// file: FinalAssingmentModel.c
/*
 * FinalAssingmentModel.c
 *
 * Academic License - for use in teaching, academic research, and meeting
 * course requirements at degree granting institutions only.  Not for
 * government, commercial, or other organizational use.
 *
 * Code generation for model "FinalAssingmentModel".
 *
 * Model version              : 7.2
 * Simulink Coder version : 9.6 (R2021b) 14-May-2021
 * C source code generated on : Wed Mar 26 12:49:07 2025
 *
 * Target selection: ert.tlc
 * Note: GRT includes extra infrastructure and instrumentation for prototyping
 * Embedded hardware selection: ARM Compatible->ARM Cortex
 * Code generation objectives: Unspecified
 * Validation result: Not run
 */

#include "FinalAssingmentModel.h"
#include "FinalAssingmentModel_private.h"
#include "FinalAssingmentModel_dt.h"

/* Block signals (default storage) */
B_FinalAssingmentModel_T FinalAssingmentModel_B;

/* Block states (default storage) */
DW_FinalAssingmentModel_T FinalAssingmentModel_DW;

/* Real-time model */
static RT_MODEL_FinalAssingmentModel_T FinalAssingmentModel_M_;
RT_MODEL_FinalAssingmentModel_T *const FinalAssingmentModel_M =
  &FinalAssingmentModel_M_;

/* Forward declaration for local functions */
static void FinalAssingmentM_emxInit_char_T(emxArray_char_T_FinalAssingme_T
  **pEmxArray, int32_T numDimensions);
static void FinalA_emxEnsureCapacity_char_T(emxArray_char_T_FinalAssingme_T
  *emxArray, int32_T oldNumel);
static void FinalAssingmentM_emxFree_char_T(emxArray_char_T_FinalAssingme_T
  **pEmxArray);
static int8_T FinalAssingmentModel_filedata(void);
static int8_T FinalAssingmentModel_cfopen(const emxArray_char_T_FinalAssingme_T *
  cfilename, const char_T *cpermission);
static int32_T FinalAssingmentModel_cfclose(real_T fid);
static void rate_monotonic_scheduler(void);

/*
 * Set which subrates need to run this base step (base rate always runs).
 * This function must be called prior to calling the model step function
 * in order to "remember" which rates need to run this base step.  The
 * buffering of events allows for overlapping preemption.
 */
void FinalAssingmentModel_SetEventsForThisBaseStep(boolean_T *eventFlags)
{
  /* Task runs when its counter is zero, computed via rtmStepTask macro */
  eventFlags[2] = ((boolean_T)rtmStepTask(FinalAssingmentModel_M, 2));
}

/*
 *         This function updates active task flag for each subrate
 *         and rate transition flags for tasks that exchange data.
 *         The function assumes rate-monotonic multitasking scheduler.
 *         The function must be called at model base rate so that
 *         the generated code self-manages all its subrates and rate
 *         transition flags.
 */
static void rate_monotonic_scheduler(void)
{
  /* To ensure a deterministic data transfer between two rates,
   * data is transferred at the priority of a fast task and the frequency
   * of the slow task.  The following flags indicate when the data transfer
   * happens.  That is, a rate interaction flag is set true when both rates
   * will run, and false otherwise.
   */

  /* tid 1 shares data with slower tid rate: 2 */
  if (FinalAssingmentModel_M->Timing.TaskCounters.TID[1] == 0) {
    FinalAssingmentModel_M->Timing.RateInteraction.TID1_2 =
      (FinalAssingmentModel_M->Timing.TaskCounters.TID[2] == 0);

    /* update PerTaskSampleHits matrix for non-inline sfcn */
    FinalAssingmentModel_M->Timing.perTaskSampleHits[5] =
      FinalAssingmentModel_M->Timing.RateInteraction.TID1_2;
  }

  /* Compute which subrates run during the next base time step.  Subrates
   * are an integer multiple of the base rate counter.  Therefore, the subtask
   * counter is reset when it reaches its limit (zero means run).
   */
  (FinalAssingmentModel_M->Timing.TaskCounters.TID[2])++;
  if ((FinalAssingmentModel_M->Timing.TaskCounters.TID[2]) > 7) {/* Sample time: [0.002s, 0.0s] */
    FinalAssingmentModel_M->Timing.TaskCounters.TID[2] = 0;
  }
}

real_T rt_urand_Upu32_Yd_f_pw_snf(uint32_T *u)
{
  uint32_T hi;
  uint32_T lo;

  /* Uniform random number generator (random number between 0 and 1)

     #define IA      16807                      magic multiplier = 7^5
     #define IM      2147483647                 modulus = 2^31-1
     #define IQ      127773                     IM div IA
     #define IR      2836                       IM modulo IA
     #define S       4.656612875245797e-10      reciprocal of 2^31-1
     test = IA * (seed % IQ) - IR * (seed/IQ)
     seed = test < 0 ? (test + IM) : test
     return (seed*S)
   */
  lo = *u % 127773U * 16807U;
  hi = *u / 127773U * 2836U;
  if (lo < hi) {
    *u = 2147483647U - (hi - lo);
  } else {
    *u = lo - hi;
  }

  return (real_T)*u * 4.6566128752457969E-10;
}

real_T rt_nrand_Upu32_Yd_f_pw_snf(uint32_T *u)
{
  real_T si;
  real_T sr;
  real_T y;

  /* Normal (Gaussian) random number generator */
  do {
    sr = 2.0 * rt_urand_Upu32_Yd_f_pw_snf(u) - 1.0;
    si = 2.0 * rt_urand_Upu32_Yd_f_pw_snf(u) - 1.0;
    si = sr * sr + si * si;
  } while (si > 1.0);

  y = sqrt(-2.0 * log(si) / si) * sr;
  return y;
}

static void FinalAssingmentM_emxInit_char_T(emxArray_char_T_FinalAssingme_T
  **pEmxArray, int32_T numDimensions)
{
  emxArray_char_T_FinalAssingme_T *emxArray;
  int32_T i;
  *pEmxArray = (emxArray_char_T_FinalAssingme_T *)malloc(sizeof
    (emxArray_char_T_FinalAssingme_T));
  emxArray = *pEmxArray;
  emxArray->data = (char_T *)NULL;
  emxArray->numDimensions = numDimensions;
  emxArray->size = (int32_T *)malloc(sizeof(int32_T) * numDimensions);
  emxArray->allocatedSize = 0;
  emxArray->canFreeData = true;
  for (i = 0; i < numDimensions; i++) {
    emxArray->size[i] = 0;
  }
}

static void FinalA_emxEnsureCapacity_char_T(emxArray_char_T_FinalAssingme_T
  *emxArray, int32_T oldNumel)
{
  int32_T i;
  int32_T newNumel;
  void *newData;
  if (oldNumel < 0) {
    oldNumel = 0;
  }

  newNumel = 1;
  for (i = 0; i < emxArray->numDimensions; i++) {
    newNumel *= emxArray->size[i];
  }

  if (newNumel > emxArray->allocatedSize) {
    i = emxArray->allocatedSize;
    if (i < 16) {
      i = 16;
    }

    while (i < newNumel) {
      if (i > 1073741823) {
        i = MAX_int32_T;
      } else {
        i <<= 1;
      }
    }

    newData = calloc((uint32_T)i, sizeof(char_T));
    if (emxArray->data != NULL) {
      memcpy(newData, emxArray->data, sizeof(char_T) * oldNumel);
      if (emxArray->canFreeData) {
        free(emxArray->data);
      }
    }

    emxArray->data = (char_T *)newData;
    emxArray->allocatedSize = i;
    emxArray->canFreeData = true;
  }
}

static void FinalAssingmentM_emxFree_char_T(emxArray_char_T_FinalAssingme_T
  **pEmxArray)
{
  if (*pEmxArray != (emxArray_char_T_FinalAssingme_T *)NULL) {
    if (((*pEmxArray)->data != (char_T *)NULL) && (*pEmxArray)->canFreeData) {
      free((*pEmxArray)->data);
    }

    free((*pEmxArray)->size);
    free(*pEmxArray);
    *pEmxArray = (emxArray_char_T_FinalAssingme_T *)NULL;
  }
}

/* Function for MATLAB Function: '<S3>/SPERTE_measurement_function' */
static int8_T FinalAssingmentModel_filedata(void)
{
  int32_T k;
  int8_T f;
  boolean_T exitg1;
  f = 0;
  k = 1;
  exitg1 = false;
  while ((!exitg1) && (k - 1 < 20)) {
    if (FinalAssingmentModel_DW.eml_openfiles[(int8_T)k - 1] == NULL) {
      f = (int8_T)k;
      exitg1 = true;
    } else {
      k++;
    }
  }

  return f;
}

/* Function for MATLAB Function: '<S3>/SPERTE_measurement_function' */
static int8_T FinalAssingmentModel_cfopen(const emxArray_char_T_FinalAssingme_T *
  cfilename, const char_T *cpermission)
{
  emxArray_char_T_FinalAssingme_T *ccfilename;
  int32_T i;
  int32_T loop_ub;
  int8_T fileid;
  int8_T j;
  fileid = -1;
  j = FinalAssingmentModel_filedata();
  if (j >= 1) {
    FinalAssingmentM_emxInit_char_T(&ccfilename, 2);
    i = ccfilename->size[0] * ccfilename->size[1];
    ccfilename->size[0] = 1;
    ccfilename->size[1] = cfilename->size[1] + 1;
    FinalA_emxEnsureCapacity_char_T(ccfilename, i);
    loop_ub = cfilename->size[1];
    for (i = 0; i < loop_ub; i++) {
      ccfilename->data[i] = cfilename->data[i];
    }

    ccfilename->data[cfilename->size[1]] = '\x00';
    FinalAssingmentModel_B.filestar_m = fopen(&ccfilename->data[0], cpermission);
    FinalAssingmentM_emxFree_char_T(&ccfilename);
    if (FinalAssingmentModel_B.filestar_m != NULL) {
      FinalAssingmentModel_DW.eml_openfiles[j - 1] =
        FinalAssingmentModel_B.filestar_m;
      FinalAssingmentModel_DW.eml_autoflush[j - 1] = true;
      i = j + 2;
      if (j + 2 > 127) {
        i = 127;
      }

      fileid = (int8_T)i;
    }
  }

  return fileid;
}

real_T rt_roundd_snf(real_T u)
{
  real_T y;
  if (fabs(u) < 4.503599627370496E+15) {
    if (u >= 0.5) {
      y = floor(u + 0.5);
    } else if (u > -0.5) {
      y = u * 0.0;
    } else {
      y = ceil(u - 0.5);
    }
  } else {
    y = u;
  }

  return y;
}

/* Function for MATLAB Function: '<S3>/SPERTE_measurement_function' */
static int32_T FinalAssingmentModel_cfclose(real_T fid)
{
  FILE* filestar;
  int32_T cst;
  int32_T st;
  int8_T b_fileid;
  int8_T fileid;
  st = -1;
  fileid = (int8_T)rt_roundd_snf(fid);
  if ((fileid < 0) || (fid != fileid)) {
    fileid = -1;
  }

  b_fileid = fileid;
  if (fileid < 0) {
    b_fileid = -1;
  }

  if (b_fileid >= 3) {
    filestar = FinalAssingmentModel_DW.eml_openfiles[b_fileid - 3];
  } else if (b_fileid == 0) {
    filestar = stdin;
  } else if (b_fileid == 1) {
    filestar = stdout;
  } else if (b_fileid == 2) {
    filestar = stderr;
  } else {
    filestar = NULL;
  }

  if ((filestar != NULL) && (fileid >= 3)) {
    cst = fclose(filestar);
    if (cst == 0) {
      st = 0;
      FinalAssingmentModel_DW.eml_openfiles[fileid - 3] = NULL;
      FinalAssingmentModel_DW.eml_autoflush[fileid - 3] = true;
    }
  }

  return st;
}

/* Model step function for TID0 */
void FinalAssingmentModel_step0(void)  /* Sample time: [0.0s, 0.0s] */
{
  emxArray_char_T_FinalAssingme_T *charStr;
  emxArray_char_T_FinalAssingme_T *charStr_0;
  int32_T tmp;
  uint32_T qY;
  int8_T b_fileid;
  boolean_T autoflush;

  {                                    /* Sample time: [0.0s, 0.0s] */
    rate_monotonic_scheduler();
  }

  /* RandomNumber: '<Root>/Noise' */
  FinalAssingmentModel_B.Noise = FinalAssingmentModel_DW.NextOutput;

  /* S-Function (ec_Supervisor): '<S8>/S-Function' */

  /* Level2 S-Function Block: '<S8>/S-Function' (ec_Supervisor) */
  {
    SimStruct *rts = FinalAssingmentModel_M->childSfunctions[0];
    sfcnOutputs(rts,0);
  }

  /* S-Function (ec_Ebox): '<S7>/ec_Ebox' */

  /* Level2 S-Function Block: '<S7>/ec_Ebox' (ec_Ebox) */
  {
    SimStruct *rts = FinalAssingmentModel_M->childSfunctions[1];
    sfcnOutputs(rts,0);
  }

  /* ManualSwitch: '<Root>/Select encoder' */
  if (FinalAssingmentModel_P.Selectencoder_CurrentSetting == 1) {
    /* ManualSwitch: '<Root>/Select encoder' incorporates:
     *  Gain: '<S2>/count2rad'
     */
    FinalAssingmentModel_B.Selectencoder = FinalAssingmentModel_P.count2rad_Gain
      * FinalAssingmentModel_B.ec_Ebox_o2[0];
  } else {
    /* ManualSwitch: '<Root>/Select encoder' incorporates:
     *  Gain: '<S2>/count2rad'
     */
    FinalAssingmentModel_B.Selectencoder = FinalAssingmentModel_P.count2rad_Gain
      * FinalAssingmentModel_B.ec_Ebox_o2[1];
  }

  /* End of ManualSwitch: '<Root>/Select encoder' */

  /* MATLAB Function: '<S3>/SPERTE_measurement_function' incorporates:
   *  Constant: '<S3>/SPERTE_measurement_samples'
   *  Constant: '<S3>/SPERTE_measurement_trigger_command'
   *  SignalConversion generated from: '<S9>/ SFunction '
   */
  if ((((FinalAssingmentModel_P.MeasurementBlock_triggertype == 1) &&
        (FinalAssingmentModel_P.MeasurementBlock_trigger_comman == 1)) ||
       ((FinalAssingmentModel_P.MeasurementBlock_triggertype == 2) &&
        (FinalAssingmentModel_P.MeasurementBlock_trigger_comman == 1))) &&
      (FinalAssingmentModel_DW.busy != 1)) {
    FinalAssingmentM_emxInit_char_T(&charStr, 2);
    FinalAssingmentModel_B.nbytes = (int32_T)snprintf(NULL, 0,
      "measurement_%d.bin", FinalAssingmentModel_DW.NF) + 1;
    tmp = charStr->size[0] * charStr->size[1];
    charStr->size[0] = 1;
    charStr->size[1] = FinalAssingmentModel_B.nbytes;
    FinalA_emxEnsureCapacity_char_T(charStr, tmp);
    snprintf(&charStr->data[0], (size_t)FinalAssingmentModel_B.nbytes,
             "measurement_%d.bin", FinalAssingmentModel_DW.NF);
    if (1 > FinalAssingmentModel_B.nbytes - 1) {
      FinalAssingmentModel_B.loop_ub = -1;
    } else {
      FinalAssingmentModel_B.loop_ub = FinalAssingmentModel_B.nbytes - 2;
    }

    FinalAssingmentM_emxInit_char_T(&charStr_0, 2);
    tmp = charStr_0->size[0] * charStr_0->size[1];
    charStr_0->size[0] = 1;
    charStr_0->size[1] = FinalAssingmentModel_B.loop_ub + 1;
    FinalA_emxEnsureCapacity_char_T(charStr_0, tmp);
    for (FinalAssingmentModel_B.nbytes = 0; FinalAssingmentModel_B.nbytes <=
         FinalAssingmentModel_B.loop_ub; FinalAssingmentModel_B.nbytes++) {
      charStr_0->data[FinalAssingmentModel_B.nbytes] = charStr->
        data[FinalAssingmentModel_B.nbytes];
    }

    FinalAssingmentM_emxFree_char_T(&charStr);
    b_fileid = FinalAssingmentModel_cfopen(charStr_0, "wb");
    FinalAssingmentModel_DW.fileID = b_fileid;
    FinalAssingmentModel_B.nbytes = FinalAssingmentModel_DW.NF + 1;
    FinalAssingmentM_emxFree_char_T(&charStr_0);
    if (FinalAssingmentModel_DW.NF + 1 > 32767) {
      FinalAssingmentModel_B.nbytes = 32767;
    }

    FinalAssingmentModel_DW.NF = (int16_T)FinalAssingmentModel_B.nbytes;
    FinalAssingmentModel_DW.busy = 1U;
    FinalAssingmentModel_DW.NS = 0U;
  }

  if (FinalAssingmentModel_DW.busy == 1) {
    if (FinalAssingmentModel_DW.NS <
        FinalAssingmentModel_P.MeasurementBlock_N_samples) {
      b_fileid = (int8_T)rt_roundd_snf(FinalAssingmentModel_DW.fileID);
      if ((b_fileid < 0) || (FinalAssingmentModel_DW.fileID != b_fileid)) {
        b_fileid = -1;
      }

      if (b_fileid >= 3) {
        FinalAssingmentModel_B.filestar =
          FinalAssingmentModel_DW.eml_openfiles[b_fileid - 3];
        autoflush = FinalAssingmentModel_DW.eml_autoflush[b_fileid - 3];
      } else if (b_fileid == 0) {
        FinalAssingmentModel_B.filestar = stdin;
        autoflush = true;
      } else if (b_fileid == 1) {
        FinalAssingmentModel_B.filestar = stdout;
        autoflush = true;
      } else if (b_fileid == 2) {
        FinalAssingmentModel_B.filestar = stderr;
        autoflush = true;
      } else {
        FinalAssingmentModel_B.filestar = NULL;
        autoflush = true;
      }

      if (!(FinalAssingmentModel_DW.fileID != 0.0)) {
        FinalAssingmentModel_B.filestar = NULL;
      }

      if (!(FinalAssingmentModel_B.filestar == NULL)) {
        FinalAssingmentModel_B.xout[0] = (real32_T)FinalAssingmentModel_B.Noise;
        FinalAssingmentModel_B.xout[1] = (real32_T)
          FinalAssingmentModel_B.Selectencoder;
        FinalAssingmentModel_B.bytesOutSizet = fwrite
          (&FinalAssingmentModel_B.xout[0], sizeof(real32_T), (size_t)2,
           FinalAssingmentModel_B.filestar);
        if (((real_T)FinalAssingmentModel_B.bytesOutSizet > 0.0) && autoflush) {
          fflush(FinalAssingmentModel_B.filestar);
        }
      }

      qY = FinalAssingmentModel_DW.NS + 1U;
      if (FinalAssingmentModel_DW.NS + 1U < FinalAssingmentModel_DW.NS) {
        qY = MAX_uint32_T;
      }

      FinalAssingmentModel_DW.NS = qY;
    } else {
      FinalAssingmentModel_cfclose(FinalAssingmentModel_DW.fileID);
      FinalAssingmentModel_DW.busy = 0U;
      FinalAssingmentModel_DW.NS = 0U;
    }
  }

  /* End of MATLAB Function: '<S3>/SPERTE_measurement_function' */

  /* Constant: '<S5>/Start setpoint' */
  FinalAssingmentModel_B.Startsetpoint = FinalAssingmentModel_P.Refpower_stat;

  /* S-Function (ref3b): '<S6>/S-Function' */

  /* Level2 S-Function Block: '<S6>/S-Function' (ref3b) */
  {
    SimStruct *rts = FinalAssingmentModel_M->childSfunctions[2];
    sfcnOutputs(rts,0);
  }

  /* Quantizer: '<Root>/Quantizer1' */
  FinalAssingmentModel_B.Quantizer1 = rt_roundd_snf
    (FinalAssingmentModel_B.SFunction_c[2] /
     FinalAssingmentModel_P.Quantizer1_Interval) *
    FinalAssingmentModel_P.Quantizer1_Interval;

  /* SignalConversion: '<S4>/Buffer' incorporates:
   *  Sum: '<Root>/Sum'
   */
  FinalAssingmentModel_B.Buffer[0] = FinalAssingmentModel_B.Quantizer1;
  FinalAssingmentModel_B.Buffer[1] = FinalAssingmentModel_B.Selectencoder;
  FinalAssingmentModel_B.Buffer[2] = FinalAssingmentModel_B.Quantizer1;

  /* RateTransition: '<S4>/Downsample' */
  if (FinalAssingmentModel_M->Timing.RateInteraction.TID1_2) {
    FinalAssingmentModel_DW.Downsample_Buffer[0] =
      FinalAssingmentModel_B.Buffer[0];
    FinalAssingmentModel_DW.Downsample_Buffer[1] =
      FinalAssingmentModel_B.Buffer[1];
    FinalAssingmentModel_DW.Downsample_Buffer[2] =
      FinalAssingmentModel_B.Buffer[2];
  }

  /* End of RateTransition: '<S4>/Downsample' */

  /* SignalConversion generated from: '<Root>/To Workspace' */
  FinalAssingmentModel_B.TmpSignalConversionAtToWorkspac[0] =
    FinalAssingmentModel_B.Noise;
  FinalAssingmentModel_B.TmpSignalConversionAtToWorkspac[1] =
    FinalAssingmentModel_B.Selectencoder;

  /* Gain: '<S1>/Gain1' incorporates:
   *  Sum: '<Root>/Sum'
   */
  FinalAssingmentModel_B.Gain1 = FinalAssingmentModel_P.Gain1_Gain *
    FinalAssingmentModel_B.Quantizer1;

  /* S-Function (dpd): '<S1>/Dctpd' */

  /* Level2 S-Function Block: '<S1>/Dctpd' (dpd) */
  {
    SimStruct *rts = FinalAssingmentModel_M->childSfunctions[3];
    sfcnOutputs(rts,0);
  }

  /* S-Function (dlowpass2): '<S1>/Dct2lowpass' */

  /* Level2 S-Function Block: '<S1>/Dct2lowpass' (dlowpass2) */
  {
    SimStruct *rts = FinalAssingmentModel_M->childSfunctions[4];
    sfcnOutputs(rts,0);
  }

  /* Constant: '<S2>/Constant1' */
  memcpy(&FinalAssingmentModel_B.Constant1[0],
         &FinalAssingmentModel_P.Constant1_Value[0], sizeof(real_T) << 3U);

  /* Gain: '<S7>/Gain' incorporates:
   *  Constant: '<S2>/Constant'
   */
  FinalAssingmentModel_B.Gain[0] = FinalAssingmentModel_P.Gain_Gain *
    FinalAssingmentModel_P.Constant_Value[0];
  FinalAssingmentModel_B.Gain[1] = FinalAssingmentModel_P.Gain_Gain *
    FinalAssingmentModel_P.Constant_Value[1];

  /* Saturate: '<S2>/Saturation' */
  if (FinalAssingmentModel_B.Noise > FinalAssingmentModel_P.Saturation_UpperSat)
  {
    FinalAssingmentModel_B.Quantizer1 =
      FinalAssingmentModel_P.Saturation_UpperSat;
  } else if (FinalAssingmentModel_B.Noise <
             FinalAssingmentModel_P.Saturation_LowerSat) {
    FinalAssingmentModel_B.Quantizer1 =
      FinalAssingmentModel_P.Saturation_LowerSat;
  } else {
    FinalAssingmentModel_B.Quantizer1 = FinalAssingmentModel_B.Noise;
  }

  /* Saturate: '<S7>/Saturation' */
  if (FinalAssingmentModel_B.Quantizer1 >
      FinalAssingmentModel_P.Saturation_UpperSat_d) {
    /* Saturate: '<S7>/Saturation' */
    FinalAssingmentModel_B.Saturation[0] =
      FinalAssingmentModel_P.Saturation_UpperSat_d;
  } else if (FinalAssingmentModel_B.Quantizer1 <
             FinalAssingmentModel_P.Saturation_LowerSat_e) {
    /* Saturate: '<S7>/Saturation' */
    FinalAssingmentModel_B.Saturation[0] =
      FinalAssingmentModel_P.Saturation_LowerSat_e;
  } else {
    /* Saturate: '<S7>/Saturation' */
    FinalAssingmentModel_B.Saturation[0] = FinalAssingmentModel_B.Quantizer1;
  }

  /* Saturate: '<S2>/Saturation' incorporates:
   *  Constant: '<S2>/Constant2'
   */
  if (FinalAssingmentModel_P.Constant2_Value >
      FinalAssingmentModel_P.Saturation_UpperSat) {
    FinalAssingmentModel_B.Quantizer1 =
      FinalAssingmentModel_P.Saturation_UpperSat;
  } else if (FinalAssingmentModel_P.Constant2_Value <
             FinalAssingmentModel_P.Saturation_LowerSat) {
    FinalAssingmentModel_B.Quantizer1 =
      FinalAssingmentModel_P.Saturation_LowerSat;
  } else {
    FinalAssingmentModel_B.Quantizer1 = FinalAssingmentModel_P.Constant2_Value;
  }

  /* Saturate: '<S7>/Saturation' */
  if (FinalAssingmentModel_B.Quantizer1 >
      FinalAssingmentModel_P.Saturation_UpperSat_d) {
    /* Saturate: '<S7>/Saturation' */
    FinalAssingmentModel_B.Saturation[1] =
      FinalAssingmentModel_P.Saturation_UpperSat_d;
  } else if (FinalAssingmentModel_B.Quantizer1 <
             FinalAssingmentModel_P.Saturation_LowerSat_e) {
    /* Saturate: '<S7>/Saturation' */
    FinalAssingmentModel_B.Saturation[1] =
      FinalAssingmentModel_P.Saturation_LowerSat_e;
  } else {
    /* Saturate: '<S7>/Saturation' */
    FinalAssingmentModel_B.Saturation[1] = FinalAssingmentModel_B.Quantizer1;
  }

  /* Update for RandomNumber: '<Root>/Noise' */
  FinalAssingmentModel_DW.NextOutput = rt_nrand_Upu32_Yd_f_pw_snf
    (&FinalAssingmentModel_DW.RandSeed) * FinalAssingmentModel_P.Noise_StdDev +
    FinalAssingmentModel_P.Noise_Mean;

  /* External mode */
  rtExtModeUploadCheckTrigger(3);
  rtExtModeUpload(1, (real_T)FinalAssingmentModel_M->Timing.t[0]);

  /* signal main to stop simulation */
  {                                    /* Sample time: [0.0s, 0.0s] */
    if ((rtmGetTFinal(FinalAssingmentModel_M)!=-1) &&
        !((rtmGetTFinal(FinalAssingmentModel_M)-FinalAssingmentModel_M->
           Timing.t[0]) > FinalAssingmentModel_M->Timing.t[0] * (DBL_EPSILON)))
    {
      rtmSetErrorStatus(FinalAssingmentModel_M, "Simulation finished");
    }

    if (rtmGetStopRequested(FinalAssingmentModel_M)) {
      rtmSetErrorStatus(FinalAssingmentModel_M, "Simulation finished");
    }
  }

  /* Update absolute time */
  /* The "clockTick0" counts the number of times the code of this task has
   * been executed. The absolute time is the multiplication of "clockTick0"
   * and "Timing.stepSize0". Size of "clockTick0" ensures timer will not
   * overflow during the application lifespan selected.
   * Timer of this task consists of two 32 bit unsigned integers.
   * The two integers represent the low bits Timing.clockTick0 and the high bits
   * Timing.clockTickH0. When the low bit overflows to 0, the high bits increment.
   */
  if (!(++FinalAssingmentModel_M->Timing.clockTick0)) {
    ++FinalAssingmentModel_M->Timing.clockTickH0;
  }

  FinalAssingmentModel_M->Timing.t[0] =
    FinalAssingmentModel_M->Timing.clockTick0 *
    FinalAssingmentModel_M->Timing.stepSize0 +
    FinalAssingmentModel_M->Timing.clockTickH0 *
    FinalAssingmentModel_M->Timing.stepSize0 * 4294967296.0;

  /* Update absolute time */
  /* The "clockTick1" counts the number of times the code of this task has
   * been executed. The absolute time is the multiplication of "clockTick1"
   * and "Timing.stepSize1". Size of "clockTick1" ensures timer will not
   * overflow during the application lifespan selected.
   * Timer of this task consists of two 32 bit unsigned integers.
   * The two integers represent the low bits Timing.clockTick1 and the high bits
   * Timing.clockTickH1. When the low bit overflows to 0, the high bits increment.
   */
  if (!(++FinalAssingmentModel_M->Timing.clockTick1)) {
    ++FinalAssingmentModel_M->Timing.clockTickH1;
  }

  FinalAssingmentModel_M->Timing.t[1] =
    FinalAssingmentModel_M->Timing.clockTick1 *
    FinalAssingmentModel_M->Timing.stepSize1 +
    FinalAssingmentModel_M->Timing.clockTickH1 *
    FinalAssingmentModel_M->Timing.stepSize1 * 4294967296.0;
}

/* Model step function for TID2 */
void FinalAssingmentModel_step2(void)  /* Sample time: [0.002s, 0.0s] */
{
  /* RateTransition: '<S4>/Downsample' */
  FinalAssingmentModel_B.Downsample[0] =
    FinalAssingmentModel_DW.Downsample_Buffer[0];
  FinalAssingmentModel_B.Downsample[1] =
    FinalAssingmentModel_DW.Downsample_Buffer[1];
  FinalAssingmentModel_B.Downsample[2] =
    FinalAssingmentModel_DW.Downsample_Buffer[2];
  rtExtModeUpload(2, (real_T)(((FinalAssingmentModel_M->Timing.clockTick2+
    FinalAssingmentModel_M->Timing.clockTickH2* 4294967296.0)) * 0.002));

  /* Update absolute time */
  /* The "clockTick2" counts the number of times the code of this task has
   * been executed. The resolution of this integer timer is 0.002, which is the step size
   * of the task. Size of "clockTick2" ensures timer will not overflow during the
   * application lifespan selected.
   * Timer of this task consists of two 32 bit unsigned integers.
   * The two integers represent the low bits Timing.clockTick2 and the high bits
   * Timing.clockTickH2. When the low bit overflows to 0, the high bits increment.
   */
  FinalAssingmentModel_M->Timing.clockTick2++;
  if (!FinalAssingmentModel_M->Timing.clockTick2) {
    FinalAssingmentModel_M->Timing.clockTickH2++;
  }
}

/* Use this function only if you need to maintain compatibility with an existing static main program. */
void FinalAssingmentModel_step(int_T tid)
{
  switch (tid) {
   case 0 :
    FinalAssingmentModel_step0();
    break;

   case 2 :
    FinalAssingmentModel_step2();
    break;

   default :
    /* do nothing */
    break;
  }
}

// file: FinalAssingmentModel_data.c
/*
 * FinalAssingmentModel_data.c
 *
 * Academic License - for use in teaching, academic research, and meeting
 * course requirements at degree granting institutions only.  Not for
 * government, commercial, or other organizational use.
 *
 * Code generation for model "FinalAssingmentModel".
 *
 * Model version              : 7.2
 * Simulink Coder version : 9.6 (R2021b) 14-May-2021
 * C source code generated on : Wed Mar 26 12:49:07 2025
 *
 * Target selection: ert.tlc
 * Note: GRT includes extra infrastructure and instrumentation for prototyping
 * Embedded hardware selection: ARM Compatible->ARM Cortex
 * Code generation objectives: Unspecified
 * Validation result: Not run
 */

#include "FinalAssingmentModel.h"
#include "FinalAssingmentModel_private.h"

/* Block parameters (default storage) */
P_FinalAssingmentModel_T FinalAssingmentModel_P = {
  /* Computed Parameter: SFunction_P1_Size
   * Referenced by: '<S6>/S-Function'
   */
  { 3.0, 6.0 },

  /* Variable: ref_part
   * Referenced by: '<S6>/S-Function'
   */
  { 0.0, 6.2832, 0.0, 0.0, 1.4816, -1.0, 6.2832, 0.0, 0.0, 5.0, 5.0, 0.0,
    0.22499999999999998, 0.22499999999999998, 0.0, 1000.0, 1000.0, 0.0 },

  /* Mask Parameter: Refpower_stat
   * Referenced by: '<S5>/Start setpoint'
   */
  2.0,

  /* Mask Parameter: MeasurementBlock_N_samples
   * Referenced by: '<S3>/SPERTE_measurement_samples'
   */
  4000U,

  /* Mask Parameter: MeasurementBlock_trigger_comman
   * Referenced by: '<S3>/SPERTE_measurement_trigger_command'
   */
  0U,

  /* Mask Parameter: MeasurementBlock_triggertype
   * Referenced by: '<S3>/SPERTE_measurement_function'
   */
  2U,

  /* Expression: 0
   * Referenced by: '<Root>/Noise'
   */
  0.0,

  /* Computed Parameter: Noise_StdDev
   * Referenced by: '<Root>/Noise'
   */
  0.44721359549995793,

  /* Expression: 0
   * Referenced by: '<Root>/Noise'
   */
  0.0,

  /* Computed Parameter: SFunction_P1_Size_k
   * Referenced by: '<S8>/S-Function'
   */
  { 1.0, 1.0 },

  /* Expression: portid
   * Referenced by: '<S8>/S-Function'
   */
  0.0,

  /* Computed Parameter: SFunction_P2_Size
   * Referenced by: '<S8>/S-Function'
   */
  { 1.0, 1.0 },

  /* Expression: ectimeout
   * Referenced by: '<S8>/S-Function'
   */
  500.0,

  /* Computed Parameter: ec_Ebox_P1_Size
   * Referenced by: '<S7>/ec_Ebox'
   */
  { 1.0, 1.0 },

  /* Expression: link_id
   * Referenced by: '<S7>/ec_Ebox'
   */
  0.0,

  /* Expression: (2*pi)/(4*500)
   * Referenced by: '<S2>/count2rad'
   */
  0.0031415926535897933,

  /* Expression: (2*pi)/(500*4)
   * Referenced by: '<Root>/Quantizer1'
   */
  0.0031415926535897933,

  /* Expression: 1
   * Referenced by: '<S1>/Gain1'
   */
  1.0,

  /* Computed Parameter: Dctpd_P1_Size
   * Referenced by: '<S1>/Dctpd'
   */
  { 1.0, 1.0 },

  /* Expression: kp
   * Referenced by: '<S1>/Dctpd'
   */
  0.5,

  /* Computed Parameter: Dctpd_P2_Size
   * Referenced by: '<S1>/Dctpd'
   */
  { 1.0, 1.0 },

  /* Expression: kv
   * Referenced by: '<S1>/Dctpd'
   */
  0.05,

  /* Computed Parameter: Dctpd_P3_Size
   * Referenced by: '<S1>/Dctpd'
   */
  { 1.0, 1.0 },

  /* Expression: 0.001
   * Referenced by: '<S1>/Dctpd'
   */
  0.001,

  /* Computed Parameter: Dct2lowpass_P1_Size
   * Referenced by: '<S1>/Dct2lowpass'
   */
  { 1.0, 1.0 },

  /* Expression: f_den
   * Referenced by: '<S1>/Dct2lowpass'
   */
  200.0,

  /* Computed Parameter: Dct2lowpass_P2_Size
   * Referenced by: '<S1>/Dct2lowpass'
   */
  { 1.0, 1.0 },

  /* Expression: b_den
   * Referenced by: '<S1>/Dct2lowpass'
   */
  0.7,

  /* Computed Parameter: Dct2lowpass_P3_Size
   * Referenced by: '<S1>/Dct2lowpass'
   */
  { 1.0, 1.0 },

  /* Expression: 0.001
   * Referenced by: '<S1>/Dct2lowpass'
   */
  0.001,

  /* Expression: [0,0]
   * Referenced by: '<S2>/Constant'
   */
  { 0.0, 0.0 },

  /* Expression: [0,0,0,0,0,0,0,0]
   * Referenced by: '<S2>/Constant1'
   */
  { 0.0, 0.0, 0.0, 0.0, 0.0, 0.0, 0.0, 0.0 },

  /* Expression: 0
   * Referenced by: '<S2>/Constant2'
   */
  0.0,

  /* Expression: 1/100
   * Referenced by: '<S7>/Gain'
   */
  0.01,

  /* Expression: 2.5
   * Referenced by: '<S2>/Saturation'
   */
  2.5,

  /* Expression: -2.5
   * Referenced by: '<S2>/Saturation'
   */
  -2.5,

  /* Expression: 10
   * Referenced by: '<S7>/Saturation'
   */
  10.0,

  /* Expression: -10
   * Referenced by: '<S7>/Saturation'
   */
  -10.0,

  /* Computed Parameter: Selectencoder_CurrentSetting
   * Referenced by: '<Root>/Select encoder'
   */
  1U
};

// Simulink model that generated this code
simulink model "FinalAssingmentModel"  (R2021b)
settings: Solver=FixedStepDiscrete  StartTime=0.0  StopTime=120  FixedStep=Ts  RelTol=1e-3  EnableMultiTasking=on
InitFcn:
  | Fs = 4000; Ts = 1/Fs; tsim = 29.9997;

== system FinalAssingmentModel ==
  note: Add more signals by expanding the Mux ports
  note: The measurement block is used to obtain high-samplerate measurements
  note: This realtime scope is used to monitor signals
  note: Always accept the reference once before starting the model.
  note: Change the variance of the noise but keep it reasonable <0.5
  Controller (motor side) : Subsystem
  Fourth Order Motion System : Subsystem
  Measurement Block : Subsystem  Description=|  Priority=-1  mask(SPERTE Lib){N_samples=4000, triggertype=2, trigger_command=0}
      | Perform on-demand measurements to file using this block.
      | 
      | It can be used in 2 ways:
      | 1) Set the mask triggertype parameter to manual and use the trigger input signal to trigger a measurement.
      | You can do this by providing a 0 to 1 transition.
      | Keep it low after you start/complete the measurement, or it will measure again.
      | A file is created with measurement_0,1,2... etc
      | 
      | 2) Keep the model running, and trigger a measurement from the commandline or Matlab script.
      | For example:
      | 
      | % How many samples to measure?
      | N_samples = Fs*5;
      | % Do the measurement
      | SPERTE_Perform_Measurement(N_samples);
      | % Get the latest file
      | file_list = SPERTE_Get_Latest_Measurement(p,1,'./data');
      | % How many signals did you record?
      | N_signals = 3;
      | % Convert the .bin to .mat and return the results
      | measurement = SPERTE_Bin_To_Mat(file_list,N_signals);
      mask prompts: N_samples "Number of samples"; trigger_command "Trigger command"
      mask help:
      | This block implements a measurement to file sink.
      | It can be used in two ways:
      | 1) Triggered from the simulink model
      | 2) Triggered from the command line
  Mux : Mux  Commented=on  Inputs=3
  Mux1 : Mux  Inputs=2
  Noise : RandomNumber  Variance=0.25  SampleTime=Ts
  Quantizer1 : Quantizer  QuantizationInterval=(2*pi)/(500*4)
  Real-time scope : Subsystem  Priority=0  Commented=on  mask(Scope){Sample_Time=1/500}
      mask prompts: Sample_Time "Scope sample time"
      mask help:
      | Realtime Scope block allows one to view the signals while the model is running.
      | The signals are downsampled to a specified sample rate (in the mask parameter) to reduce communication overhead.
  Ref power : Subsystem  mask(On/Off Switch){stat=Off}
      mask prompts: stat "Switch"
  Select encoder : ManualSwitch
  Subsystem : Subsystem  mask(Ref3){}
  Sum : Sum  Inputs=|+-
  Sum1 : Sum  Inputs=|++
  Terminator : Terminator
  Terminator1 : Terminator
  To Workspace : ToWorkspace  VariableName=simout  SampleTime=-1
  wires:
  Fourth Order Motion System/1(Motor [rad]) -> Select encoder/1
  Fourth Order Motion System/2(Load [rad]) -> Select encoder/2
  Select encoder/1 -> Mux/2, Mux1/2
  Sum1/1 -> Fourth Order Motion System/1(Motor [v])
  Controller (motor side)/1(control signal) -> ?
  Sum/1 -> Mux/3, Controller (motor side)/1(error)
  Quantizer1/1 -> Mux/1, Sum/1
  Ref power/1(On/Off) -> Subsystem/1(start)
  Subsystem/3(pos) -> Quantizer1/1
  Mux/1 -> Real-time scope/1(In1)
  Noise/1 -> Sum1/2, Mux1/1
  Mux1/1 -> To Workspace/1, Measurement Block/2(Signals)
  Subsystem/1(acc) -> Terminator/1
  Subsystem/2(vel) -> Terminator1/1

== system FinalAssingmentModel/Controller (motor side) ==
  error : Inport
  Dct2lowpass : S-Function  FunctionName=dlowpass2  Parameters=f_den, b_den, 0.001  SFunctionDeploymentMode=off  EnableBusSupport=off  mask(dctools){f_den=200, b_den=0.7}
      mask prompts: f_den "Pole [Hz]"; b_den "Damping pole [-]"
      mask help: This block implements a discrete time 2nd order lowpass filter.
  Dctpd : S-Function  FunctionName=dpd  Parameters=kp, kv, 0.001  SFunctionDeploymentMode=off  EnableBusSupport=off  mask(dctools){kp=0.5, kv=0.05}
      mask help: This block implements a discrete time pd filter.
  Gain1 : Gain  SaturateOnIntegerOverflow=on  OutDataTypeStr=Inherit: Same as input  ParamDataTypeStr=Inherit: Same as input
  control signal : Outport
  wires:
  Dct2lowpass/1 -> control signal/1
  Gain1/1 -> Dctpd/1
  error/1 -> Gain1/1
  Dctpd/1 -> Dct2lowpass/1

== system FinalAssingmentModel/Fourth Order Motion System ==
  Motor [v] : Inport
  Constant : Constant  Value=[0,0]
  Constant1 : Constant  Value=[0,0,0,0,0,0,0,0]
  Constant2 : Constant  Value=0
  Demux : Demux  Outputs=2
  Ethercat E-box : Subsystem  Priority=-2  mask(Sperte Lib){link_id=0}
      mask prompts: link_id "Link ID of the specific ebox"
      mask help:
      | This block implements a single E-box device.
      | Ensure that if you have multiple E-box devices that they each have an unique link_id.
      |
      | You MUST have an Ethercat Initialize block in your model to be able to use this block.
  Ethercat Supervisor : Subsystem  Description=Must be executed first, keep at -1 priority (highest)  Priority=-3  mask(Sperte Lib){portid=0, ectimeout=500}
      mask prompts: portid "Ethernet port number for the Ethercat protocol (default 0 = eth0)"; ectimeout "Timeout of the Ethercat protocol in microseconds."
      mask help:
      | This block initializes the Ethercat connection on the Raspberry Pi.
      |
      | This enables you to use multiple E-box devices by including multiple blocks of the "Ethercat E-box" type.
  Mux : Mux  Inputs=2
  Saturation : Saturate  UpperLimit=2.5  LowerLimit=-2.5
  Terminator : Terminator
  Terminator1 : Terminator
  Terminator2 : Terminator
  count2rad : Gain  Gain=(2*pi)/(4*500)
  Motor [rad] : Outport
  Load [rad] : Outport  Port=2
  wires:
  Ethercat E-box/1(ADC [v]) -> Terminator1/1
  Ethercat E-box/2(ENC [count]) -> count2rad/1
  Constant/1 -> Ethercat E-box/2(PWM [%])
  Mux/1 -> Saturation/1
  count2rad/1 -> Demux/1
  Motor [v]/1 -> Mux/1
  Constant2/1 -> Mux/2
  Demux/1 -> Motor [rad]/1
  Demux/2 -> Load [rad]/1
  Ethercat E-box/3(DI [1/0]) -> Terminator/1
  Constant1/1 -> Ethercat E-box/3(DO [1/0])
  Saturation/1 -> Ethercat E-box/1(DAC [v])
  Ethercat Supervisor/1(Status) -> Terminator2/1

== system FinalAssingmentModel/Measurement Block ==
  Trigger : Inport
  Signals : Inport  Port=2
  SPERTE_measurement_function : MATLAB Function  TreatAsAtomicUnit=on
  SPERTE_measurement_samples : Constant  Value=N_samples  OutDataTypeStr=uint32
  SPERTE_measurement_trigger_command : Constant  Value=trigger_command  OutDataTypeStr=uint8
  Status : Outport
  wires:
  SPERTE_measurement_samples/1 -> SPERTE_measurement_function/4(N_samples)
  SPERTE_measurement_trigger_command/1 -> SPERTE_measurement_function/3(trigger_command)
  Signals/1 -> SPERTE_measurement_function/1(u)
  Trigger/1 -> SPERTE_measurement_function/2(trigger_manual)
  SPERTE_measurement_function/1(status) -> Status/1

== system FinalAssingmentModel/Real-time scope ==
  note: The default scope sample rate is 500 Hz.
      | This can be changed by right-click on the Realtime Scope block.
      | Then selecting -> Mask -> Mask parameters.
  In1 : Inport
  Buffer : SignalConversion  OverrideOpt=off
  Downsample : RateTransition  OutPortSampleTime=Sample_Time
  Live_Scope : Scope
  wires:
  In1/1 -> Buffer/1
  Downsample/1 -> Live_Scope/1
  Buffer/1 -> Downsample/1

== system FinalAssingmentModel/Ref power ==
  Start setpoint : Constant  Value=stat
  On/Off : Outport
  wires:
  Start setpoint/1 -> On/Off/1

== system FinalAssingmentModel/Subsystem ==
  start : Inport
  Demux : Demux  Outputs=3
  S-Function : S-Function  FunctionName=ref3b  Parameters=ref_part  SFunctionDeploymentMode=off  EnableBusSupport=off
  acc : Outport
  vel : Outport  Port=2
  pos : Outport  Port=3
  wires:
  S-Function/1 -> Demux/1
  Demux/1 -> acc/1
  Demux/2 -> vel/1
  Demux/3 -> pos/1
  start/1 -> S-Function/1

== system FinalAssingmentModel/Fourth Order Motion System/Ethercat E-box ==
  DAC [v] : Inport
  PWM [%] : Inport  Port=2
  DO [1/0] : Inport  Port=3
  Gain : Gain  Gain=1/100
  Saturation : Saturate  UpperLimit=10  LowerLimit=-10
  ec_Ebox : S-Function  FunctionName=ec_Ebox  Parameters=link_id  SFunctionDeploymentMode=off  EnableBusSupport=off  mask{link_id=link_id}
      mask prompts: link_id "link_id >= 0"
  ADC [v] : Outport
  ENC [count] : Outport  Port=2
  DI [1/0] : Outport  Port=3
  wires:
  Gain/1 -> ec_Ebox/2
  Saturation/1 -> ec_Ebox/1
  ec_Ebox/3 -> DI [1/0]/1
  ec_Ebox/1 -> ADC [v]/1
  ec_Ebox/2 -> ENC [count]/1
  DAC [v]/1 -> Saturation/1
  DO [1/0]/1 -> ec_Ebox/3
  PWM [%]/1 -> Gain/1

== system FinalAssingmentModel/Fourth Order Motion System/Ethercat Supervisor ==
  note: Status, 0 = Operational, 1 = error
  S-Function : S-Function  FunctionName=ec_Supervisor  Parameters=portid,ectimeout  SFunctionDeploymentMode=off  EnableBusSupport=off
  Status : Outport
  wires:
  S-Function/1 -> Status/1

== matlab function FinalAssingmentModel/Measurement Block/SPERTE_measurement_function ==
function status = perform_measurement(u, trigger_manual, trigger_command, triggertype, N_samples)

%% Persistent variables
persistent fileID NF busy NS

% Init parameters
if isempty(NF)
    NF = int16(0);
end
if isempty(NS)
    NS = uint32(0);
end
if isempty(fileID)
    fileID = 0;
end
if isempty(busy)
    busy = uint8(0);
end

%% Check the triggers
if ( (triggertype == 0 && trigger_manual == 1) || (triggertype == 1 && trigger_command == 1) || (triggertype == 2 && (trigger_command == 1 || trigger_manual == 1) ) )
    if busy == 1
        % We are already busy, nothing to do
    else
        % We should start a new one
        fileID = fopen(sprintf('measurement_%d.bin',NF),'w');  
        NF = NF + 1;
        busy = uint8(1);
        NS = uint32(0);
    end
end

% We have started a measurement
if busy == 1
    if NS < N_samples 
        % Here we write the sample, in single precision float
        fwrite(fileID,u,'single');
        NS = NS + uint32(1);
    else
       % We have N samples already, we are done
       fclose(fileID);
       busy = uint8(0);
       NS = uint32(0);
    end
      
end
    % Output state
    status = uint8(busy);
end
